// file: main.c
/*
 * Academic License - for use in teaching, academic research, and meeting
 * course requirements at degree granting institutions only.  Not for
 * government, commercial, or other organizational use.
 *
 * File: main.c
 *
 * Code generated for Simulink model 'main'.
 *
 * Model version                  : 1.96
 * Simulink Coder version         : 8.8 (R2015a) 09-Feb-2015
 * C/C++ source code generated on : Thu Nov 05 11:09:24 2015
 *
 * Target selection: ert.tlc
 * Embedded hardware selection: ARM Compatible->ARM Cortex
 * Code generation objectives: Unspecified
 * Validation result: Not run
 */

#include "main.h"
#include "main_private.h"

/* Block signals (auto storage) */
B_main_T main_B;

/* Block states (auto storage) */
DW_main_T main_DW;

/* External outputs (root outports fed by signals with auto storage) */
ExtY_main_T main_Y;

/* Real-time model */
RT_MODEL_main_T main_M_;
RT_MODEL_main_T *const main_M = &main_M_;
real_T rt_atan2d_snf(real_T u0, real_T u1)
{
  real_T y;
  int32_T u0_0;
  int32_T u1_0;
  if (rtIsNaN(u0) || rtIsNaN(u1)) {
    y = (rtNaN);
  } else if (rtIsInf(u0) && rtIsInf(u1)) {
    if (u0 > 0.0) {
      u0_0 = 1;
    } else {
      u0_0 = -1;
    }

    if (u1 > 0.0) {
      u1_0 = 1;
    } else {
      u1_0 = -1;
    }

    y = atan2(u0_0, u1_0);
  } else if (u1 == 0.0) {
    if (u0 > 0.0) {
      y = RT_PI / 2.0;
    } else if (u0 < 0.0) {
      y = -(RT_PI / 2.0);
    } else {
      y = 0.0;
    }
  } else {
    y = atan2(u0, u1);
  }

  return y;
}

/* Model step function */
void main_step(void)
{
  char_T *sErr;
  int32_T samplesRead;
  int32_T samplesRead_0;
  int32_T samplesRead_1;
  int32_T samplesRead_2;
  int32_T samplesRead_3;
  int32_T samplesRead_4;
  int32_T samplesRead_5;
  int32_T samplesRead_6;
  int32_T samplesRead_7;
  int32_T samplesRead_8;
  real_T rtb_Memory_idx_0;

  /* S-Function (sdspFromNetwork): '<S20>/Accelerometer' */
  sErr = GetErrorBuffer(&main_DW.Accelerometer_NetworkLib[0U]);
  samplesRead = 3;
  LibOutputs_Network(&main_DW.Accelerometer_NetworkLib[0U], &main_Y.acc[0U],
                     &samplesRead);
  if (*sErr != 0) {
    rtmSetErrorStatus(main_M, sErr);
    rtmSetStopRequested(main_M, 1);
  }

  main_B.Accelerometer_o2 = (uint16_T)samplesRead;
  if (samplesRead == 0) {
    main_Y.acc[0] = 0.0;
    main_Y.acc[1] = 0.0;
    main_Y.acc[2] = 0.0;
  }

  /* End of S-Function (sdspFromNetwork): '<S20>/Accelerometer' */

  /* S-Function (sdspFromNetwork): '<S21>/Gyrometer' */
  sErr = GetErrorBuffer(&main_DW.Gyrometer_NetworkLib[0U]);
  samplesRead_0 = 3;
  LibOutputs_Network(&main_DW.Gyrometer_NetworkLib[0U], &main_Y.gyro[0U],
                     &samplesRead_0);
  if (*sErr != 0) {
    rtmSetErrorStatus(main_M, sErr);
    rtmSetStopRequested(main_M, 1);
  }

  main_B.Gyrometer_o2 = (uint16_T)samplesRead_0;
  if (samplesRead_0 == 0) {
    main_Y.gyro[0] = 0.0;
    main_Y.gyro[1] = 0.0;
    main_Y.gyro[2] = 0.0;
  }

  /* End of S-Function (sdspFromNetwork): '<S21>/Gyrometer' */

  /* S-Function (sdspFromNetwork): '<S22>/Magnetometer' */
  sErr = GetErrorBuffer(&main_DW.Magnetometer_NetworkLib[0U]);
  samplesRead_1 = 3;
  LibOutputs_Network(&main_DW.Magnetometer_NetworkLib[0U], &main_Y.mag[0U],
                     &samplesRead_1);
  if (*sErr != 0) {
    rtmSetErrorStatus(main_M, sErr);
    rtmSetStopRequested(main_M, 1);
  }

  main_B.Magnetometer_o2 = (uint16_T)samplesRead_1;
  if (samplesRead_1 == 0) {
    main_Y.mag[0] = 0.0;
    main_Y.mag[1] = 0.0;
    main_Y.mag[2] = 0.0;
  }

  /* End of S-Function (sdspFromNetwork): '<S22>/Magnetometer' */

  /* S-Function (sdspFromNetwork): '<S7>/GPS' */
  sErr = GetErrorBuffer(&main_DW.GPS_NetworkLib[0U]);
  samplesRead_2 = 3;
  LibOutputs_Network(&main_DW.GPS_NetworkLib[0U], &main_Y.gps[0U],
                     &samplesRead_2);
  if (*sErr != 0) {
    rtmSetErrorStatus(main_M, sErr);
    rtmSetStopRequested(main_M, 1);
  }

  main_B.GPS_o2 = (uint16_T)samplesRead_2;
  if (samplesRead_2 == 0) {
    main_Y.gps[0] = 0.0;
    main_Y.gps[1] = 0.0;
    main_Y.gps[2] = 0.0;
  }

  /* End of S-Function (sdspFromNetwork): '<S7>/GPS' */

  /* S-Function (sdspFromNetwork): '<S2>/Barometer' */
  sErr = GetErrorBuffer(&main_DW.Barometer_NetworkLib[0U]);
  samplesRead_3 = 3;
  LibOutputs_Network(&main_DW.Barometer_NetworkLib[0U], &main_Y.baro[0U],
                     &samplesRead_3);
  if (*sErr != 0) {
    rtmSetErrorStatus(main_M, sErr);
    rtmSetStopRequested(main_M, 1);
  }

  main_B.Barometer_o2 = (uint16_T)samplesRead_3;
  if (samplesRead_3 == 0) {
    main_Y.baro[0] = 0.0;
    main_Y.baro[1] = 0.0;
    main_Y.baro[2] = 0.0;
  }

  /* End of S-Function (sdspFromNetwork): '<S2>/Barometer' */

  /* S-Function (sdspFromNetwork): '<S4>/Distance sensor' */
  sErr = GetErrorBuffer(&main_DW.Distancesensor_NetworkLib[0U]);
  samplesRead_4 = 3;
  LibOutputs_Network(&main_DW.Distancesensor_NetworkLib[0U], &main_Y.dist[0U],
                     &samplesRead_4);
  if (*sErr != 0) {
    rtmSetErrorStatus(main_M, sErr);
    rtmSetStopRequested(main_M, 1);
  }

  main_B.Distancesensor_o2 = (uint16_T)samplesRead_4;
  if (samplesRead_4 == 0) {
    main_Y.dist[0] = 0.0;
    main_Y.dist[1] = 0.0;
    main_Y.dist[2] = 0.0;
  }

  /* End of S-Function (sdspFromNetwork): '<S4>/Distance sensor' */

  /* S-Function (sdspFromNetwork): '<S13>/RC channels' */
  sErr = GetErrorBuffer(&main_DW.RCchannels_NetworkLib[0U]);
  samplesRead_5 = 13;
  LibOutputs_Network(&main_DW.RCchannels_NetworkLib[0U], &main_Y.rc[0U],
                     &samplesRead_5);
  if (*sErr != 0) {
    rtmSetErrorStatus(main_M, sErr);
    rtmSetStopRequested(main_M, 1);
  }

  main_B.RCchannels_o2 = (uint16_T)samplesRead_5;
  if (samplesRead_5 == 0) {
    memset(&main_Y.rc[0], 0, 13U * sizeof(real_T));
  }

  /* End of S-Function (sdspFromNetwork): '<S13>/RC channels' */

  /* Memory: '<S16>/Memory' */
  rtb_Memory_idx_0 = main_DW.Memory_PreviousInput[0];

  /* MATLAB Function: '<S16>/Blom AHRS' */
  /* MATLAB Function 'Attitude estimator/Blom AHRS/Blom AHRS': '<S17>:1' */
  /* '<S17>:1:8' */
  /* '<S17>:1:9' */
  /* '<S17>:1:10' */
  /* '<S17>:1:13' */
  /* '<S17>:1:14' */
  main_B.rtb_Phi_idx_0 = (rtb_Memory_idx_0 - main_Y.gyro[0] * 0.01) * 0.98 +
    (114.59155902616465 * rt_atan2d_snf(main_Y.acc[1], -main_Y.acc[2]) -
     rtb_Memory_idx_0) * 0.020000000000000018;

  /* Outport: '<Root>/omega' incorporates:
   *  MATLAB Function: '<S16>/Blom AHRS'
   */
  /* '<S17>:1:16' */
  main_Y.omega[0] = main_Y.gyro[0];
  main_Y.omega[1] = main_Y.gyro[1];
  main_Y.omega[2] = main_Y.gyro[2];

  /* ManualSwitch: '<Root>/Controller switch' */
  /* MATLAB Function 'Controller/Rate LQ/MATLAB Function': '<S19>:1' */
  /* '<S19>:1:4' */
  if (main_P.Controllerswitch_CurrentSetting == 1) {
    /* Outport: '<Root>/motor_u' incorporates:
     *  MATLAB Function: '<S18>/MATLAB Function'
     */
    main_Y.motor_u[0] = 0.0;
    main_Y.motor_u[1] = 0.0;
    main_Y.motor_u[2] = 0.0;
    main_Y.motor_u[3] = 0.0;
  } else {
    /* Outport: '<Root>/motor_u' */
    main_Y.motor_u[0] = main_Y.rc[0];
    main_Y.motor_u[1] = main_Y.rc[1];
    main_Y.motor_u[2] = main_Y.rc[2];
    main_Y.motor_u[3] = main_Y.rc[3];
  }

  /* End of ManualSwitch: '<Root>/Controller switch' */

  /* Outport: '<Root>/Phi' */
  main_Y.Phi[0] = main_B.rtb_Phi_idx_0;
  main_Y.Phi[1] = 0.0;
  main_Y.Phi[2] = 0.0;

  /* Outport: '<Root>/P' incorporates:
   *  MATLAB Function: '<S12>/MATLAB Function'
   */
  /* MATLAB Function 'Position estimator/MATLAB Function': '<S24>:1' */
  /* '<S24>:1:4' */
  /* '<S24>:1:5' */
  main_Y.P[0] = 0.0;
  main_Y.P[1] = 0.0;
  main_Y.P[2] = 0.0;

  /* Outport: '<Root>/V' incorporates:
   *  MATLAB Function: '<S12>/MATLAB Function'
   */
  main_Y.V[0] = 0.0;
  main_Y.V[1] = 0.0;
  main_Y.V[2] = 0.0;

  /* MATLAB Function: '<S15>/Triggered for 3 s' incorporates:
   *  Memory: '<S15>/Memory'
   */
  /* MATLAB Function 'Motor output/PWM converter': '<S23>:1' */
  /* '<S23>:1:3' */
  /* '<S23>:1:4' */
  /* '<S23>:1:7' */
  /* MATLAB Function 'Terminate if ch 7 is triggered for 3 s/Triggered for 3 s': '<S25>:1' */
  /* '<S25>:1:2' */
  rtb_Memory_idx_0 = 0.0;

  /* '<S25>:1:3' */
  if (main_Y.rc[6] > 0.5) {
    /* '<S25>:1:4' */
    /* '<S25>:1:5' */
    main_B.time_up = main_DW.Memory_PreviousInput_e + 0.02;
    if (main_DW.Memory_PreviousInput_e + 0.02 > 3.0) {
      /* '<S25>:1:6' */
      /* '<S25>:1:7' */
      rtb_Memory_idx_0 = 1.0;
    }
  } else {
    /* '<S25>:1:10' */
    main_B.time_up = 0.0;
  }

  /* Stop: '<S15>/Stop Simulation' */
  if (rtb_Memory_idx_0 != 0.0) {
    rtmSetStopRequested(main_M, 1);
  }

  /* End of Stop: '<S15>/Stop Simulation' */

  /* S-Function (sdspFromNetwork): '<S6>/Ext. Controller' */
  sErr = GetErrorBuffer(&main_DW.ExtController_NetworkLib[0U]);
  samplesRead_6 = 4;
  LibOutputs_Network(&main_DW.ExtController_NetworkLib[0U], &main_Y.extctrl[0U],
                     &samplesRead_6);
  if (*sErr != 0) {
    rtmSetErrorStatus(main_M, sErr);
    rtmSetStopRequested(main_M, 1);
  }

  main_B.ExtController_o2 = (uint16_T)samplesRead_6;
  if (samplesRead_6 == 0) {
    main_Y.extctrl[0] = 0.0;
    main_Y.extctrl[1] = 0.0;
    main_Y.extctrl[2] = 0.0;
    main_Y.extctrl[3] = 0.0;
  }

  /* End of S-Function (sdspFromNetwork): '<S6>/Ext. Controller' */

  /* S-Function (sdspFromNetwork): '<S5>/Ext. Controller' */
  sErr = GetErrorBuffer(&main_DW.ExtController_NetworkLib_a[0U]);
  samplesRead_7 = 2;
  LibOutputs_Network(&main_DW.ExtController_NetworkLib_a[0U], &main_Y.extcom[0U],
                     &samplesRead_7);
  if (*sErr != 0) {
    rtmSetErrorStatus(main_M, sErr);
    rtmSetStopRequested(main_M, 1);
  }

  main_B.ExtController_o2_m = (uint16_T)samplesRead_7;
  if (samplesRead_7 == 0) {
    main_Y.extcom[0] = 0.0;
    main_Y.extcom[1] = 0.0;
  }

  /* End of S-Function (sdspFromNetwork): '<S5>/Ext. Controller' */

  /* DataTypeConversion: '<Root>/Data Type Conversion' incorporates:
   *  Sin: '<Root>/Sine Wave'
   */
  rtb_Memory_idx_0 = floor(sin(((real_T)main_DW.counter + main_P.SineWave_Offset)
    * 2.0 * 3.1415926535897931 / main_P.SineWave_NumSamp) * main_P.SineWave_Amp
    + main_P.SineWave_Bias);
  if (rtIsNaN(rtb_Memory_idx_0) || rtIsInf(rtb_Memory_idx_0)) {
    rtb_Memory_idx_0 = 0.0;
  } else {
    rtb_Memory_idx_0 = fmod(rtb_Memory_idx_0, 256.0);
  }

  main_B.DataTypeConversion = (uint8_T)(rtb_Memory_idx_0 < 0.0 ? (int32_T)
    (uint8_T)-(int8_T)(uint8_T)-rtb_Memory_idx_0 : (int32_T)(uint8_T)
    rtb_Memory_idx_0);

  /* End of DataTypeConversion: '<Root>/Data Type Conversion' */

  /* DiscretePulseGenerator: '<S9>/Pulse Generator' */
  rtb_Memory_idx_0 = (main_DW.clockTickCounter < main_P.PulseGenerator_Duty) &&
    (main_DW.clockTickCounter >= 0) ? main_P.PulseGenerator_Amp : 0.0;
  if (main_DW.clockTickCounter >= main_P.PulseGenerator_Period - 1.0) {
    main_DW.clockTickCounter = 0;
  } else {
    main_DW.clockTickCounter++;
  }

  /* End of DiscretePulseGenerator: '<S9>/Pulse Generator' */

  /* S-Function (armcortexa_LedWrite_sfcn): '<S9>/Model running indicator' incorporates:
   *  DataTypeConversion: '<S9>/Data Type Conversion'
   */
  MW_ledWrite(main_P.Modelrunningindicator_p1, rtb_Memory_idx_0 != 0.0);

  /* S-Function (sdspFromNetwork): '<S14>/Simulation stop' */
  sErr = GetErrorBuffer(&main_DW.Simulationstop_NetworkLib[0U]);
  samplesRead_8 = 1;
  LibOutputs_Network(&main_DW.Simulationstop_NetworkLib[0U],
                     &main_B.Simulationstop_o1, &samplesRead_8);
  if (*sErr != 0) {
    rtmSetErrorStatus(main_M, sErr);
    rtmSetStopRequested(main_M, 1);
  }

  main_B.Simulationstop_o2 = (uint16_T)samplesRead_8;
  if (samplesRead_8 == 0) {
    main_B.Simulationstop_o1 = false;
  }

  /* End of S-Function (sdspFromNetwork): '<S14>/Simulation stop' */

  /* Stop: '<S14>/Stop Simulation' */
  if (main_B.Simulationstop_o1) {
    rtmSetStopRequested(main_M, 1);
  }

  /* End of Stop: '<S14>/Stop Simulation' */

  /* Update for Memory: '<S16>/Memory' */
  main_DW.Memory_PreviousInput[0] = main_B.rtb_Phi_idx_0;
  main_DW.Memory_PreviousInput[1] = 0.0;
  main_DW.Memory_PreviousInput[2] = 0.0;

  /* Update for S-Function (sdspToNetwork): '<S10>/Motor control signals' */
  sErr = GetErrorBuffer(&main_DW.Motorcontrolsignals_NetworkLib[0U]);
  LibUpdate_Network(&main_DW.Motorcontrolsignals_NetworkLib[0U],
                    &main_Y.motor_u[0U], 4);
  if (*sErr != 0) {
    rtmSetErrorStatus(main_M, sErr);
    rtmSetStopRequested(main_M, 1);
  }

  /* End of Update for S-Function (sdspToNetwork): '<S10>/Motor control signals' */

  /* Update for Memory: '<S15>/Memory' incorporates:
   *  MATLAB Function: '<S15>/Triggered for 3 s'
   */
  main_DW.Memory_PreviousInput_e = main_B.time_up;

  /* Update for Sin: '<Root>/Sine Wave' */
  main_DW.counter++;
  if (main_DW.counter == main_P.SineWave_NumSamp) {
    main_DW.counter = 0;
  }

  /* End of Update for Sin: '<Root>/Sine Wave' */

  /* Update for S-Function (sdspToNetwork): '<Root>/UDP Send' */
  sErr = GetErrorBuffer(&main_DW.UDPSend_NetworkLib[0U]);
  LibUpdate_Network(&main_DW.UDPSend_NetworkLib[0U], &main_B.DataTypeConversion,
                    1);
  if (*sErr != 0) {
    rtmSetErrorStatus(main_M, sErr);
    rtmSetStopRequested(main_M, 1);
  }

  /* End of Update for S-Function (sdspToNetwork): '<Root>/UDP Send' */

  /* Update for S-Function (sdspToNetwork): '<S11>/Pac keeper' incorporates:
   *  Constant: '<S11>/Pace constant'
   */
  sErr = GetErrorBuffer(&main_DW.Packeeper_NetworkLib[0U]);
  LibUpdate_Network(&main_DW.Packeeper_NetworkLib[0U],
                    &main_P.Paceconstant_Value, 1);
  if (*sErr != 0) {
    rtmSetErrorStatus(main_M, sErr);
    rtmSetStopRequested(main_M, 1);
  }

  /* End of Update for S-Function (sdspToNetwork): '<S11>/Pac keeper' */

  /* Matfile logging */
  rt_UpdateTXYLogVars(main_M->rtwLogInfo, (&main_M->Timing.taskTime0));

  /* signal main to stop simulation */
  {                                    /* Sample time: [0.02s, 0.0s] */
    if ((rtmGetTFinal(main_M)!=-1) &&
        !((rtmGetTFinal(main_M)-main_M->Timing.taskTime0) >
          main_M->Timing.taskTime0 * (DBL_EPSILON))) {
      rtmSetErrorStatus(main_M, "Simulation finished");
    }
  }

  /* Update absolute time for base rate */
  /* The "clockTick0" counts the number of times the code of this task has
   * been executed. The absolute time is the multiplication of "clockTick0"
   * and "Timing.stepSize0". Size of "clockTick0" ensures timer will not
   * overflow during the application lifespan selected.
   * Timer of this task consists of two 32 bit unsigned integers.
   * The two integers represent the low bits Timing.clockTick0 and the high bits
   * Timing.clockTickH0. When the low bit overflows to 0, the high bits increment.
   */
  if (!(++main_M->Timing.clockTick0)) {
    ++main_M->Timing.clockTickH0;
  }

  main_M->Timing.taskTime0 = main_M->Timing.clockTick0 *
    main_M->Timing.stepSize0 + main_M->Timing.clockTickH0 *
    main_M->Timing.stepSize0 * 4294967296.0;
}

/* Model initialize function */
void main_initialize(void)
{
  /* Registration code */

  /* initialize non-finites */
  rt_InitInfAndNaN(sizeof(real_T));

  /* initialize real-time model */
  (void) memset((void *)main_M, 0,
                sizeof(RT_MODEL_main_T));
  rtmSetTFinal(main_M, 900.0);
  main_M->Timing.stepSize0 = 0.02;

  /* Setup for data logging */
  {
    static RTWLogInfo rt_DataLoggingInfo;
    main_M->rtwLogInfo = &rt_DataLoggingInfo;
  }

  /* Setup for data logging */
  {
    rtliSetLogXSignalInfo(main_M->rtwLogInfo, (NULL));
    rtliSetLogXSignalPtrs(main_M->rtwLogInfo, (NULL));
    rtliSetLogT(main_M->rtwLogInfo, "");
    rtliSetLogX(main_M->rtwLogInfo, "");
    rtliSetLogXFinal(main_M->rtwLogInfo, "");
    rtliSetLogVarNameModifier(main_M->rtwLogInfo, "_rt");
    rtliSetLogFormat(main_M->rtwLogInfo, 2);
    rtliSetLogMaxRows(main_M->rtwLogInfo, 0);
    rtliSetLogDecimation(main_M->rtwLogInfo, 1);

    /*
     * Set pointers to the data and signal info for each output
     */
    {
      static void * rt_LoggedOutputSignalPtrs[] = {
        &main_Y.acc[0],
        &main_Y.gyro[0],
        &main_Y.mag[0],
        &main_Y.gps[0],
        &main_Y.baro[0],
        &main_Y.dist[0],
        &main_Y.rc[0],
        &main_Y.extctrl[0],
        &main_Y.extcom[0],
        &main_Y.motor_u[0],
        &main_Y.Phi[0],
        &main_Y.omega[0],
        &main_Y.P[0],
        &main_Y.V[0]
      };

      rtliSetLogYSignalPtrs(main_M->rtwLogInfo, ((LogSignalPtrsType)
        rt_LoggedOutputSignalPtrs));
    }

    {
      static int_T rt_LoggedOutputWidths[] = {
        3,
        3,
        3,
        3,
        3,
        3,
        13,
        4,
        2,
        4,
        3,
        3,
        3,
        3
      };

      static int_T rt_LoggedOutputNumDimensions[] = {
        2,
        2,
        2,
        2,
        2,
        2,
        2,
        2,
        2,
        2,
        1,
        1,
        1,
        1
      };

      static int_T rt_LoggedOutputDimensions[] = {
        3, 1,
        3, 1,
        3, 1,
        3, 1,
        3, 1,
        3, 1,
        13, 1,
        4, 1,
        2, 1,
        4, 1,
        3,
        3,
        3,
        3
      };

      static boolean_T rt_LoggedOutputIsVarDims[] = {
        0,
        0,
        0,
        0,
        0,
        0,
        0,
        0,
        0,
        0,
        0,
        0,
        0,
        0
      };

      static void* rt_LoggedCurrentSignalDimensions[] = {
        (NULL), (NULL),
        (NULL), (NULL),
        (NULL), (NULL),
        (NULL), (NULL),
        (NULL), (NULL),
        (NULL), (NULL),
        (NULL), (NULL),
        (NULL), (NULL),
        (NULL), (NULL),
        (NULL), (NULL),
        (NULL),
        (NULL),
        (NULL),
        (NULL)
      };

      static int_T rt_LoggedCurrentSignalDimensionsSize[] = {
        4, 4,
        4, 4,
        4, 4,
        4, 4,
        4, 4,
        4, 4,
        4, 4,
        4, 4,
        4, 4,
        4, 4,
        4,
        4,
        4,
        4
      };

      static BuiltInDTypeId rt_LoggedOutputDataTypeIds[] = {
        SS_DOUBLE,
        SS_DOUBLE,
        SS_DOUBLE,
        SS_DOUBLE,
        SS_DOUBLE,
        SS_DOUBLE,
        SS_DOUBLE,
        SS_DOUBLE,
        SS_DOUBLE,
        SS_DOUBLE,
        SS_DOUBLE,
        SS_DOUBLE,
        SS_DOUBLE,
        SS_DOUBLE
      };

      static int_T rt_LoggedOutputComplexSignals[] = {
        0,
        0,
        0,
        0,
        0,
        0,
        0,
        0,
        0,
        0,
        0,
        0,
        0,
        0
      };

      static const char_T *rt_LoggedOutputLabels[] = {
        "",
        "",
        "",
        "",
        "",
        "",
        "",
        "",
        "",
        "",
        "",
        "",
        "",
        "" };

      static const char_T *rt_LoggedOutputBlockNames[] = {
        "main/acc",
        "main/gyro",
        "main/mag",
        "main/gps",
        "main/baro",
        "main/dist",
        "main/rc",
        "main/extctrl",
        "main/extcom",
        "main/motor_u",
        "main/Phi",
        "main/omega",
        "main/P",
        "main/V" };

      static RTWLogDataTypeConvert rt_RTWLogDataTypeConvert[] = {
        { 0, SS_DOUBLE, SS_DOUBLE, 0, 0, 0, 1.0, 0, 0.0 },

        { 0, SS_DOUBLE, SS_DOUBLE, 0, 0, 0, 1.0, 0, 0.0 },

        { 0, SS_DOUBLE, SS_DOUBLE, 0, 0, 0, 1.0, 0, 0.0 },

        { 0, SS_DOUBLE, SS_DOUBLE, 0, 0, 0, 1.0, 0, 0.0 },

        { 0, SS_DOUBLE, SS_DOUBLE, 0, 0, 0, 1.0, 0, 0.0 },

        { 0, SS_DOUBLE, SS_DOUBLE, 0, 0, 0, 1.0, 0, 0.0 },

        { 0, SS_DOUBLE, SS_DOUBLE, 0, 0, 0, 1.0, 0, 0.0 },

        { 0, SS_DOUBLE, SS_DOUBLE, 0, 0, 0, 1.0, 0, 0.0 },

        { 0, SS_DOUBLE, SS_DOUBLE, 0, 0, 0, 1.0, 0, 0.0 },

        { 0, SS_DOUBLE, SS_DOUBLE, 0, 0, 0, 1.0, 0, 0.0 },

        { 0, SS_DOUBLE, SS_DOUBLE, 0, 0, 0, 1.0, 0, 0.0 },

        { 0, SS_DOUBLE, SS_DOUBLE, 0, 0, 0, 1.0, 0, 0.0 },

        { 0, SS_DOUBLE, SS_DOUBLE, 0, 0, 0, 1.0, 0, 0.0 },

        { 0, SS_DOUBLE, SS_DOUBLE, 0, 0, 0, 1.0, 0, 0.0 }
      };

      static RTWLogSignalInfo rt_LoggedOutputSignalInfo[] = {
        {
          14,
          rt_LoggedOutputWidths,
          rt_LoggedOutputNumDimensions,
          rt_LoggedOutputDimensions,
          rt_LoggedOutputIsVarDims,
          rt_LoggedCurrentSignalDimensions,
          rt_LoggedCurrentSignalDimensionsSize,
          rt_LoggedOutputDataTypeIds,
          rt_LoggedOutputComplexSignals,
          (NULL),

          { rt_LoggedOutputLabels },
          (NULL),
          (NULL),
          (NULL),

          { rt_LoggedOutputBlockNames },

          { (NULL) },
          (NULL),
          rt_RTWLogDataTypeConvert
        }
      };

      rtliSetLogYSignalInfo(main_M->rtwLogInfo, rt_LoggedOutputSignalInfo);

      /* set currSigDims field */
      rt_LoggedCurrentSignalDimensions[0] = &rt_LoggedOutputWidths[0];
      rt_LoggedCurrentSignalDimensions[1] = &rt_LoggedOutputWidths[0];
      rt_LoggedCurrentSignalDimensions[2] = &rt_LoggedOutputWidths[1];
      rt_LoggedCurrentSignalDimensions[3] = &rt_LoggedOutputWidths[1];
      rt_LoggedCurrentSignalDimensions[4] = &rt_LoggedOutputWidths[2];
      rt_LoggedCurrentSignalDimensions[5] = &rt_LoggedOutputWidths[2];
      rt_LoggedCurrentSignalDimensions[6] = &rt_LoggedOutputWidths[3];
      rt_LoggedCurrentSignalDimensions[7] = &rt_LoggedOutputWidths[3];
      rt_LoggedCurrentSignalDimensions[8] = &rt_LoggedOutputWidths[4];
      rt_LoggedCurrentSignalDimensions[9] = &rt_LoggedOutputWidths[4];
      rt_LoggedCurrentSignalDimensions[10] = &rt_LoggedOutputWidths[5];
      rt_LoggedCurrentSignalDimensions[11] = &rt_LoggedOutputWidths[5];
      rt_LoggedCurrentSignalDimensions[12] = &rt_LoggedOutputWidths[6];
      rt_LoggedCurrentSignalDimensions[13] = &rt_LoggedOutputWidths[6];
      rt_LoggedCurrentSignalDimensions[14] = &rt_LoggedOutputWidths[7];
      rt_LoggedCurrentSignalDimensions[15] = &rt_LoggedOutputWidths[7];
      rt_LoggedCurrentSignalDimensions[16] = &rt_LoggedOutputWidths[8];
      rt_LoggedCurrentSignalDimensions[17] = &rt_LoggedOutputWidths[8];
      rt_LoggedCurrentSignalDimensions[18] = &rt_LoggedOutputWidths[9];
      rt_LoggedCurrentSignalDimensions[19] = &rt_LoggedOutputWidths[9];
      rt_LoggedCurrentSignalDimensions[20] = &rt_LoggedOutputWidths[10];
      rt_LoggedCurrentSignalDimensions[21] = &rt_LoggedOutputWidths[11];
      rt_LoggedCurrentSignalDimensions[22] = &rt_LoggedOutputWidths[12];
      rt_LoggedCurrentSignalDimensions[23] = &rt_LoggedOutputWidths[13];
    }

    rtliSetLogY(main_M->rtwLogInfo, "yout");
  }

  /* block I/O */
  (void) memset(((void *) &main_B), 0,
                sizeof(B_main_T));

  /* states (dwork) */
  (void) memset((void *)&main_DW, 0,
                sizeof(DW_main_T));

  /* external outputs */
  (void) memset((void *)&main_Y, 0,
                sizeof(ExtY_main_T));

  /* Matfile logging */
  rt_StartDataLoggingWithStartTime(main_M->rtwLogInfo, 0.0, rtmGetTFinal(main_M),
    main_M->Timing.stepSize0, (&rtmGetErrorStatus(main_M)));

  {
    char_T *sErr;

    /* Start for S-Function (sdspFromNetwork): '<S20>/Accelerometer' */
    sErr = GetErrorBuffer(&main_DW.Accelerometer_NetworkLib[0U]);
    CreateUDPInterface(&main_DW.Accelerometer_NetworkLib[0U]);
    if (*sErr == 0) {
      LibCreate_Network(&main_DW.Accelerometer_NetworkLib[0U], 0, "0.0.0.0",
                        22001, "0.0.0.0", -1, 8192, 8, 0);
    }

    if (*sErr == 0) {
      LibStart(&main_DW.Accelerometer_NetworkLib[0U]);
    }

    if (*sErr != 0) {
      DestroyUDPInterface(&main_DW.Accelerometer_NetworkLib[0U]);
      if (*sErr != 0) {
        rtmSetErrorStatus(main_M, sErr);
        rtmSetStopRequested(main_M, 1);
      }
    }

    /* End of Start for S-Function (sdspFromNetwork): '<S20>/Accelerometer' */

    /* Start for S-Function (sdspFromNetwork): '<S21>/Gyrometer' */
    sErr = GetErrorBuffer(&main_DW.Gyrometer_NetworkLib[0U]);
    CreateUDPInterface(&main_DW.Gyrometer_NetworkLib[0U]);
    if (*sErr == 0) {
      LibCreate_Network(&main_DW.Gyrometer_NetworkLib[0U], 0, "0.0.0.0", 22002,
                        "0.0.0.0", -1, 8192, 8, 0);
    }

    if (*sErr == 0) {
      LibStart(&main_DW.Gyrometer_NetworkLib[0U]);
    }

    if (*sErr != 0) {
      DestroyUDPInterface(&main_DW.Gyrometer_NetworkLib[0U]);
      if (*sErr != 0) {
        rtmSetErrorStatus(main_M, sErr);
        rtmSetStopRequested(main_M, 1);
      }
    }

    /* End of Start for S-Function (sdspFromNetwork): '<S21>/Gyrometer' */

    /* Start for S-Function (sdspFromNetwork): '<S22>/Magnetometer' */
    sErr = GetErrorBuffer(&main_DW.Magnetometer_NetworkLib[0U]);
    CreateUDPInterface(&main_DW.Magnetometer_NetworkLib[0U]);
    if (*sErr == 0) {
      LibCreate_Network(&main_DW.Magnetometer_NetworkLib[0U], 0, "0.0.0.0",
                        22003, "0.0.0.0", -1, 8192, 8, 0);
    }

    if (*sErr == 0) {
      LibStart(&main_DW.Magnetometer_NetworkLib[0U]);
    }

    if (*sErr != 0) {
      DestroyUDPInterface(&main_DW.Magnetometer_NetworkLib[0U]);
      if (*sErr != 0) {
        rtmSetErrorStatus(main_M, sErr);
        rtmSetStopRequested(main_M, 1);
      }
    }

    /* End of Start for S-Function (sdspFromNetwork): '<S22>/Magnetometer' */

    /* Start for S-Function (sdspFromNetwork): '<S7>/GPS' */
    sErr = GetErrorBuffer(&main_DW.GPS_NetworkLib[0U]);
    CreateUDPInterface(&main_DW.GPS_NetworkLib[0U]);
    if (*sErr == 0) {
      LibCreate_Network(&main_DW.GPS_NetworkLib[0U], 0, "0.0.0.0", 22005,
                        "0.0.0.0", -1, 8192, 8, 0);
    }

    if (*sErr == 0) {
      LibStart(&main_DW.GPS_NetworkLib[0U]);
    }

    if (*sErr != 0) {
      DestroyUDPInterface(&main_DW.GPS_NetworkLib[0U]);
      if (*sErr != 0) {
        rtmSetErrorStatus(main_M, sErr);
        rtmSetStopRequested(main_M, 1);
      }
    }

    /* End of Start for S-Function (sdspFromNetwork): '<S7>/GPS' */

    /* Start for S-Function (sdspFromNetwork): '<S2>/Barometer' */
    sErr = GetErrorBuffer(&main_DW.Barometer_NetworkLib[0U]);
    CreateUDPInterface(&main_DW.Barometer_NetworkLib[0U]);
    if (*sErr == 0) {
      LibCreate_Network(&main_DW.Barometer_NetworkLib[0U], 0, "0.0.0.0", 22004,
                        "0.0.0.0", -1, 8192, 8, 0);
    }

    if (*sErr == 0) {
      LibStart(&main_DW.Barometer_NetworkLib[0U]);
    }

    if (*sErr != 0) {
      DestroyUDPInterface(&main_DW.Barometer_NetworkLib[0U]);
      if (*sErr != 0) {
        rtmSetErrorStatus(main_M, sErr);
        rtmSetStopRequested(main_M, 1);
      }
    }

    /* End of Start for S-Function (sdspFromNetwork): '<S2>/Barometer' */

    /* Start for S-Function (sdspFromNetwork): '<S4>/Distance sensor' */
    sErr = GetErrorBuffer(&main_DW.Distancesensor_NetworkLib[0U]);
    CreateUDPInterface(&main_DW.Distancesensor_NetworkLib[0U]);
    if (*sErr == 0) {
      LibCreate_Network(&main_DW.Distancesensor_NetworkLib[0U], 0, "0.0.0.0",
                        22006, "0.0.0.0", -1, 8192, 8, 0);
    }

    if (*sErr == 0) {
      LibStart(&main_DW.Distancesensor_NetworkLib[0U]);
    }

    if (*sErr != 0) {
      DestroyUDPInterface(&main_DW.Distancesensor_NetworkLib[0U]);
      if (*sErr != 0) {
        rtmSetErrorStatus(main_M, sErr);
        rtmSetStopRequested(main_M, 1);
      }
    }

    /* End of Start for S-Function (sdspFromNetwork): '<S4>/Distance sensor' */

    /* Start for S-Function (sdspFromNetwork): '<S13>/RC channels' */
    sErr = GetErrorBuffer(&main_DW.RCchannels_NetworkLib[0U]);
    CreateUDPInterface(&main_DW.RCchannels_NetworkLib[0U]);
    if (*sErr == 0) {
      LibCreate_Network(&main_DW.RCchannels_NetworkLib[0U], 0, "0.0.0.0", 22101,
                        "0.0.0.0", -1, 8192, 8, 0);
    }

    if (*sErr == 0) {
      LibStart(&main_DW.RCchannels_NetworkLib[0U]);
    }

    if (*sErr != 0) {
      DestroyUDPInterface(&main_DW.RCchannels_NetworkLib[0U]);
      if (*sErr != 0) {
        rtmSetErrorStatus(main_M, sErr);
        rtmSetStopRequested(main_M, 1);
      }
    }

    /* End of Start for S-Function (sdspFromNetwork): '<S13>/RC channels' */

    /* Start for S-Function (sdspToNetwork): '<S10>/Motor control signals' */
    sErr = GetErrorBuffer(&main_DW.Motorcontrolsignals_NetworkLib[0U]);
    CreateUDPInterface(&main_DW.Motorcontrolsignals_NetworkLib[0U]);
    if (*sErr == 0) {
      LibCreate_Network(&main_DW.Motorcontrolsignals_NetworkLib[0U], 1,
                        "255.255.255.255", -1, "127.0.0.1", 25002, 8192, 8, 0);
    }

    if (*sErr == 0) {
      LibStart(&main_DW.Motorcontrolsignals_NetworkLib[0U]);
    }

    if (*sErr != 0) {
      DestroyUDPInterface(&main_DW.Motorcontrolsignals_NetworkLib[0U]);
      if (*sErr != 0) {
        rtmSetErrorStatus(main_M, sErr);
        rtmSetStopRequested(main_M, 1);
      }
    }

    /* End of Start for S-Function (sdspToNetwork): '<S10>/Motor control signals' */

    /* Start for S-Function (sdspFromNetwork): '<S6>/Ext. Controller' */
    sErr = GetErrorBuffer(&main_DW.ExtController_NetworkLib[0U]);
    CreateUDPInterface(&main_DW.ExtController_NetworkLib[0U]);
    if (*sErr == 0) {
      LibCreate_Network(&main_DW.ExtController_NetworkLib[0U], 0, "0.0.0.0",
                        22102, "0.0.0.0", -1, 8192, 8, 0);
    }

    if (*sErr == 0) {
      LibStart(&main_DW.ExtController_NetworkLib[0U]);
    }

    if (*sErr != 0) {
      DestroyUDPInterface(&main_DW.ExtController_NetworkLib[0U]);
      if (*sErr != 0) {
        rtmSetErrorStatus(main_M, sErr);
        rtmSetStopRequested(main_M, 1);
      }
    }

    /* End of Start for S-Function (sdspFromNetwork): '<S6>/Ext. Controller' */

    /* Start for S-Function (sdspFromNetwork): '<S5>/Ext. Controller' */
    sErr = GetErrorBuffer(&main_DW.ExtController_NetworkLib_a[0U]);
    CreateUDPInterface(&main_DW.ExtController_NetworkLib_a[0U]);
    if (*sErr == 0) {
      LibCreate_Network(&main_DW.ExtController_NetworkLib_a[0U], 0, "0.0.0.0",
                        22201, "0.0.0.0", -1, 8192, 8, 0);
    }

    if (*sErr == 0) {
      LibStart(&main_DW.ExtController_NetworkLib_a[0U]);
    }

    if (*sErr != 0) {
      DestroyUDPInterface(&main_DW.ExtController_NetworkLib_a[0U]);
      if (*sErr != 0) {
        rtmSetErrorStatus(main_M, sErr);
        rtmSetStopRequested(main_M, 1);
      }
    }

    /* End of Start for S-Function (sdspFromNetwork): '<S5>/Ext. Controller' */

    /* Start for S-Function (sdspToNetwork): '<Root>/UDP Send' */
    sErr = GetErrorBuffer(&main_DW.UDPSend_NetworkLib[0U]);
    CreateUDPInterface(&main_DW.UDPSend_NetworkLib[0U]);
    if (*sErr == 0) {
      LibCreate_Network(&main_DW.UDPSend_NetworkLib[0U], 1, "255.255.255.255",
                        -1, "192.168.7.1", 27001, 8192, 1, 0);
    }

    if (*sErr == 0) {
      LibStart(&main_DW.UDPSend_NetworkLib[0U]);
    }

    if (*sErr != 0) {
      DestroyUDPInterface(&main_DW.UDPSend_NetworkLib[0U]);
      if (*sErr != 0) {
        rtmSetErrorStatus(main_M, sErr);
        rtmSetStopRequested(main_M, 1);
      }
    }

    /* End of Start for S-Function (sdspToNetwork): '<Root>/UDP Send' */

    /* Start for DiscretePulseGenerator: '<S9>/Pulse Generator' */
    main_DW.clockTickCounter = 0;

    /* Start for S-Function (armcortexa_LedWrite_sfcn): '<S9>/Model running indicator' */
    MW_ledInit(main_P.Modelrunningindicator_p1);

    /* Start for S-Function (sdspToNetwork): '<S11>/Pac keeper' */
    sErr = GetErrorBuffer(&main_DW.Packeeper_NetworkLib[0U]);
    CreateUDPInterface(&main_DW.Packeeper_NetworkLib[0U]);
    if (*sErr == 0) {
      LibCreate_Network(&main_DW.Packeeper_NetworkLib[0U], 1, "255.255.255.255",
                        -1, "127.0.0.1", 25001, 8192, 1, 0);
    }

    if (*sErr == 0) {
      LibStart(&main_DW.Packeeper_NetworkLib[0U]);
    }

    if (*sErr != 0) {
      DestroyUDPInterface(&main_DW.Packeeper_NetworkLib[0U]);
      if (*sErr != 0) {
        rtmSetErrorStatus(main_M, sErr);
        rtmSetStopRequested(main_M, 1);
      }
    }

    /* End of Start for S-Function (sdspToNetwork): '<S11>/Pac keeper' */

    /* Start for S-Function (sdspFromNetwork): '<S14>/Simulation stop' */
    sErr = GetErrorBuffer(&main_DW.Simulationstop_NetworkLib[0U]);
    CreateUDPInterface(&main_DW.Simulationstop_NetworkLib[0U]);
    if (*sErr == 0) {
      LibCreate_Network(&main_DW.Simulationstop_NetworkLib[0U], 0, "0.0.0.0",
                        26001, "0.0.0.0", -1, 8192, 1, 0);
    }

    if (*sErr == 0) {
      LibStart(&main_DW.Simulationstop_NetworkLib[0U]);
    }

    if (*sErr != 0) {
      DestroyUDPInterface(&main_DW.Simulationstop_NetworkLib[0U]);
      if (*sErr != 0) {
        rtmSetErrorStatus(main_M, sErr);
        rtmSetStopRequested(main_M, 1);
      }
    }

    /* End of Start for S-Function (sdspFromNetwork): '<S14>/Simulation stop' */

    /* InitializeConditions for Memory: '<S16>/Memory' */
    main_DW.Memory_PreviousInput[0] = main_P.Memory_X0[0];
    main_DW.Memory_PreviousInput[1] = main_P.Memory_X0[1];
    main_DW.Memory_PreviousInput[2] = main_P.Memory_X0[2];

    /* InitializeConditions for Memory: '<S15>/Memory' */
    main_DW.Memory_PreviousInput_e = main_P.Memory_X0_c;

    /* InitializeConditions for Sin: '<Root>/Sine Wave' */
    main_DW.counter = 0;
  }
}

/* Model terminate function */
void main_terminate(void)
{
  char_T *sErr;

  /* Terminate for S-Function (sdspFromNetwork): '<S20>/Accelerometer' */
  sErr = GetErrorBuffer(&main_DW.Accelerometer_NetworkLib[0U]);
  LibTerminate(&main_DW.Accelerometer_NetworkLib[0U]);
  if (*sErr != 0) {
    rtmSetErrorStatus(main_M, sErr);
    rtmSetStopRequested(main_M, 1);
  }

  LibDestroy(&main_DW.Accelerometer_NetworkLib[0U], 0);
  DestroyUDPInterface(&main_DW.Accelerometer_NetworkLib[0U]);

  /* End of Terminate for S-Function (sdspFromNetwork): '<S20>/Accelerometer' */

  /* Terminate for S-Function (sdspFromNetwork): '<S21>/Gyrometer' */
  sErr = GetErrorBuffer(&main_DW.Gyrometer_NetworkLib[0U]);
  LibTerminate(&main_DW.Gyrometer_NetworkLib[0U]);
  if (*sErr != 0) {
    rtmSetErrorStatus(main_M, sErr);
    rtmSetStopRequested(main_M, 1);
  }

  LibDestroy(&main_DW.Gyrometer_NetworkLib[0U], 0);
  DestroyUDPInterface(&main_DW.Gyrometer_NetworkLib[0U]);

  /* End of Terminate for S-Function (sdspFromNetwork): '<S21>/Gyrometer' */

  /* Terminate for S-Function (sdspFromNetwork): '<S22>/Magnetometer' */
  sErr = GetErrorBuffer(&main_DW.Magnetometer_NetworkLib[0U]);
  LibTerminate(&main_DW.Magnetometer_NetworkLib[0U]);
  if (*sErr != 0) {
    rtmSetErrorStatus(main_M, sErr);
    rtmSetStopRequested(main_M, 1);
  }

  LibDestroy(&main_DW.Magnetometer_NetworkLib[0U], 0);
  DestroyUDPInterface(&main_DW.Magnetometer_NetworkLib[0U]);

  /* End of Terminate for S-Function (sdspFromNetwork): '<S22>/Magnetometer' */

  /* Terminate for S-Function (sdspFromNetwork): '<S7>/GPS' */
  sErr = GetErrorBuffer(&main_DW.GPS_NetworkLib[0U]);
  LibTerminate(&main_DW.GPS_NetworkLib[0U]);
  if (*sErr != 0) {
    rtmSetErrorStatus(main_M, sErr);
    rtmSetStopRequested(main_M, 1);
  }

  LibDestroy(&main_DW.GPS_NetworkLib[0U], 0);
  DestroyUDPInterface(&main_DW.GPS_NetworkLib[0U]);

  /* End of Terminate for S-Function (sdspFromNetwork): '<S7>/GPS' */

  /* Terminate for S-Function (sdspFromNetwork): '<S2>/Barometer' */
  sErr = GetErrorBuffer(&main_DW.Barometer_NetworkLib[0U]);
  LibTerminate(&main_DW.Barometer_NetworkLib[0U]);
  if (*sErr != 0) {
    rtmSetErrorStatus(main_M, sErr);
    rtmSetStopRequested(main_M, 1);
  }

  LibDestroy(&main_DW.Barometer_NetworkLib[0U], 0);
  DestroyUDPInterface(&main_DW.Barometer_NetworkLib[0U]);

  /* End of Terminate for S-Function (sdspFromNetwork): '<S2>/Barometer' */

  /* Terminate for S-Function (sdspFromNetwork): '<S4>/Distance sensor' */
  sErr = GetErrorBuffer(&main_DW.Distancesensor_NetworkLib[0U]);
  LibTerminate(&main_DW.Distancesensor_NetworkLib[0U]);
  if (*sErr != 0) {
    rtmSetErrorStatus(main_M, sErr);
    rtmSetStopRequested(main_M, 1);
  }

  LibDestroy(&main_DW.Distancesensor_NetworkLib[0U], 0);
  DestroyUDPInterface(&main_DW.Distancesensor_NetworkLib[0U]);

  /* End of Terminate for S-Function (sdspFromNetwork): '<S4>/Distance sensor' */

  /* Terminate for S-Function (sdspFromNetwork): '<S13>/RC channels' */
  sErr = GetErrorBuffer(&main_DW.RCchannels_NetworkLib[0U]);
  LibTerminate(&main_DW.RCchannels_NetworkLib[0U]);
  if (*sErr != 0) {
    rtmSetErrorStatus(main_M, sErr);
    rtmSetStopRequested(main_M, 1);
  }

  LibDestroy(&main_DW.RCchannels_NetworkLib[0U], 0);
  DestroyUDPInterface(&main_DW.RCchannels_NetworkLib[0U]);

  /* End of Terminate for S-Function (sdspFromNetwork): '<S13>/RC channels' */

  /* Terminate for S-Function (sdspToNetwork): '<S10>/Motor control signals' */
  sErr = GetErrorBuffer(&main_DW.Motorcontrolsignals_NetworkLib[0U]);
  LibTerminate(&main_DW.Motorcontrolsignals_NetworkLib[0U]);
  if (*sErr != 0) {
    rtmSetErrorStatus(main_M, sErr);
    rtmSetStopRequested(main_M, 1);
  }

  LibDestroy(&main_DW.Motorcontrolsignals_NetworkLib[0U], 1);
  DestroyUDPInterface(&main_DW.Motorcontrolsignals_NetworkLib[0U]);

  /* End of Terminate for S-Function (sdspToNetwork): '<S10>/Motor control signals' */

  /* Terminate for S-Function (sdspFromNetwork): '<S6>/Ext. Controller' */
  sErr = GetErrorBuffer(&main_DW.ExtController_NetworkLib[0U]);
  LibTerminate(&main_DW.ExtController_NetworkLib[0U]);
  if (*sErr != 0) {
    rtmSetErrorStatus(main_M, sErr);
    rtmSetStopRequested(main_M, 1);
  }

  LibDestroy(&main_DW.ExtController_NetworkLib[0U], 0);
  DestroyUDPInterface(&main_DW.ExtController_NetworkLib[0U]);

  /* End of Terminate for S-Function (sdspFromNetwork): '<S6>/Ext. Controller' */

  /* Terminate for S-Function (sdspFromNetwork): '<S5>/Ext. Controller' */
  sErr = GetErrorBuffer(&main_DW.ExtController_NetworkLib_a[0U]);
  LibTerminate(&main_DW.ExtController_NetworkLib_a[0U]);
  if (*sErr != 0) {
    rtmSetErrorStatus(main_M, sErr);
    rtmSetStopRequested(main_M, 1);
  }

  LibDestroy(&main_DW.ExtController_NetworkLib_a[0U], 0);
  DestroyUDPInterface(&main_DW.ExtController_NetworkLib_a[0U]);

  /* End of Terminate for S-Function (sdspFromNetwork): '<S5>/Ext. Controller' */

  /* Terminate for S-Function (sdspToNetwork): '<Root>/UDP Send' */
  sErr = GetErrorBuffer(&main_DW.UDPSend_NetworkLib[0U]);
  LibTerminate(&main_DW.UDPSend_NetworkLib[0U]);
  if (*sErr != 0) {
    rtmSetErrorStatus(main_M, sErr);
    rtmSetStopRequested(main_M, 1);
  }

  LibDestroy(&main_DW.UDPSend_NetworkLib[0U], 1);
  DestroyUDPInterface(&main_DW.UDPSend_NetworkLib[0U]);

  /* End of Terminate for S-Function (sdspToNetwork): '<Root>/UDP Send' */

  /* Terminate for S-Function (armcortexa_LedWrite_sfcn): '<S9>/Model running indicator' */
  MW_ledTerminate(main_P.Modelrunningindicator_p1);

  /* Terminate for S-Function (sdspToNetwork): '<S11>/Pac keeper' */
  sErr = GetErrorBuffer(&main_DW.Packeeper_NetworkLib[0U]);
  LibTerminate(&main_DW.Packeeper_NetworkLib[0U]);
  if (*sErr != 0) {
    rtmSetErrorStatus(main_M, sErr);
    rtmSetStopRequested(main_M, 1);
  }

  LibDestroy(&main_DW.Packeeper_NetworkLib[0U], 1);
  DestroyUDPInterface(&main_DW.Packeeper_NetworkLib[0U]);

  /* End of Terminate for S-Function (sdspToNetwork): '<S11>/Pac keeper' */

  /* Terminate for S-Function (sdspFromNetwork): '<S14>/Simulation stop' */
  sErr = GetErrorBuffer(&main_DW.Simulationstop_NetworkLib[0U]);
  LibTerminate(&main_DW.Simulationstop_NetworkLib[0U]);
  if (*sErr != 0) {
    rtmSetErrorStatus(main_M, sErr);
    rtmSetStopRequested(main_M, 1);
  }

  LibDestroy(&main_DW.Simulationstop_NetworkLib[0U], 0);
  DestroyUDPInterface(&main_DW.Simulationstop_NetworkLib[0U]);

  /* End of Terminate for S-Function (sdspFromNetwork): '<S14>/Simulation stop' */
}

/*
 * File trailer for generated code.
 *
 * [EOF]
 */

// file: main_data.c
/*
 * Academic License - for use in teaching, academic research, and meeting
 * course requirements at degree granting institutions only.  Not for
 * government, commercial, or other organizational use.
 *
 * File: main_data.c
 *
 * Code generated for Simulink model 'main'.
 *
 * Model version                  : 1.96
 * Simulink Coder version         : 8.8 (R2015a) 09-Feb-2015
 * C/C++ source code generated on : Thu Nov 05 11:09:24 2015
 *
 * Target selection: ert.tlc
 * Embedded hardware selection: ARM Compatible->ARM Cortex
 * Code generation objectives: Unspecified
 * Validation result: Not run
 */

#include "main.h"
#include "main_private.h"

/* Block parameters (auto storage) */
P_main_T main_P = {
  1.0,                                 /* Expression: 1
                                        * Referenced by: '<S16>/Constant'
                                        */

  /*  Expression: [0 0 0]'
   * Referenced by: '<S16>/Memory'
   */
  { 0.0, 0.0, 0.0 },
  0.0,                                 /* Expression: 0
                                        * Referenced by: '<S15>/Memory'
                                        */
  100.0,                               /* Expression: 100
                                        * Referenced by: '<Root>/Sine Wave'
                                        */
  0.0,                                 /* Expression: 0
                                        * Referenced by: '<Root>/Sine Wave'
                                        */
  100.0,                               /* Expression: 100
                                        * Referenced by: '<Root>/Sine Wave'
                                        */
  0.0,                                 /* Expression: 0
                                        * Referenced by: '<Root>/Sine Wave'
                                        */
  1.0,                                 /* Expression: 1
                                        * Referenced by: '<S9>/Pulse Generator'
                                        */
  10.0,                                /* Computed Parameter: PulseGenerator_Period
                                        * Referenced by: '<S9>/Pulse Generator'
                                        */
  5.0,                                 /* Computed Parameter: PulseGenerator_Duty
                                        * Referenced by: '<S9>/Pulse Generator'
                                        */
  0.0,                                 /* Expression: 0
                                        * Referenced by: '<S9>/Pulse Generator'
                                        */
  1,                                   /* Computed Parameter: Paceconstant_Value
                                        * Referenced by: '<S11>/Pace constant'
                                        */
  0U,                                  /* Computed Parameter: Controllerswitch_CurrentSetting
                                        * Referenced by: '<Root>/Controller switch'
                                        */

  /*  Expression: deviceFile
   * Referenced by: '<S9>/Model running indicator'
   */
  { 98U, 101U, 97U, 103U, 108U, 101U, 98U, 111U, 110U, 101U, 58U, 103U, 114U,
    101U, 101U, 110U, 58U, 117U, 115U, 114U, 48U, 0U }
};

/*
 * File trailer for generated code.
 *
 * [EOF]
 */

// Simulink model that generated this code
simulink model "main"  (R2015a)
settings: Solver=ode3  StartTime=0.0  StopTime=time_end  FixedStep=time_step  RelTol=1e-3
values from neighbouring files (symbols this model uses):
  time_step = .02    (= 0.02)    [main.m]
libraries: dspnetwork x13, ec_arm_cortex_a_lib x1

== system main ==
  Attitude estimator : Subsystem  Variant=on  OverrideUsingVariant=Variant
  Barometer : Subsystem
  Controller : Subsystem  Variant=on  OverrideUsingVariant=Variant
  Controller switch : ManualSwitch  CurrentSetting=0
  Data Type Conversion : DataTypeConversion  OutDataTypeStr=uint8
  Distance sensor : Subsystem
  Ext. commands : Subsystem
  Ext. controller : Subsystem
  GPS : Subsystem
  IMU : Subsystem
  Model running indicator : Subsystem
  Motor output : Subsystem
  Pace keeper : Subsystem
  Position estimator : Subsystem
  RC channels : Subsystem
  Simulation stopper from UDP : Subsystem
  Sine Wave : Sin  SineType=Sample based  Amplitude=100  Samples=100  SampleTime=time_step  VectorParams1D=off
  Terminate if ch 7 is triggered for 3 s : Subsystem
  UDP Send : dspnetwork/UDP Send  remoteURL='192.168.7.1'  remotePort=27001  localURL='255.255.255.255'  localPortSource=Automatically determine  localPort=-1  sampletime=-1  blockPlatform=BeagleBone  separateLengthPort=0
  ch 1-4 : Selector  InputPortWidth=13  Indices=[1 2 3 4]
  acc : Outport
  gyro : Outport  Port=2
  mag : Outport  Port=3
  gps : Outport  Port=4
  baro : Outport  Port=5
  dist : Outport  Port=6
  rc : Outport  Port=7
  extctrl : Outport  Port=8
  extcom : Outport  Port=9
  motor_u : Outport  Port=10
  Phi : Outport  Port=11
  omega : Outport  Port=12
  P : Outport  Port=13
  V : Outport  Port=14
  wires:
  IMU/1(acc) -> acc/1, Attitude estimator/1(acc)
  IMU/2(gyro) -> gyro/1, Attitude estimator/2(gyro)
  IMU/3(mag) -> mag/1, Attitude estimator/3(mag)
  GPS/1(gps) -> gps/1, Position estimator/1(gps)
  Distance sensor/1(dist) -> Position estimator/3(dist), dist/1
  RC channels/1(rc) -> rc/1, Terminate if ch 7 is triggered for 3 s/1(channels), Controller/5(r), ch 1-4/1
  Ext. controller/1(extctrl) -> extctrl/1
  Ext. commands/1(extcom) -> extcom/1
  Position estimator/1(P) -> Controller/3(P), P/1
  Attitude estimator/1(Phi) -> Controller/1(Phi), Phi/1
  Attitude estimator/2(omega) -> omega/1, Controller/2(omega)
  Position estimator/2(V) -> V/1, Controller/4(V)
  Controller/1(motor_u) -> Controller switch/1
  Barometer/1(baro) -> baro/1, Position estimator/2(baro)
  Controller switch/1 -> motor_u/1, Motor output/1(motor_u)
  ch 1-4/1 -> Controller switch/2
  Sine Wave/1 -> Data Type Conversion/1
  Data Type Conversion/1 -> UDP Send/1

== system main/Attitude estimator ==
  note: 1) Add Subsystem or Model blocks as valid variant choices.
      | 2) You cannot connect blocks at this level. At simulation, connectivity is automatically
      | determined, based on the active variant and port name matching.
  acc : Inport
  gyro : Inport  Port=2
  mag : Inport  Port=3
  Blom AHRS : Subsystem  VariantControl=Variant
  Phi : Outport
  omega : Outport  Port=2

== system main/Barometer ==
  Barometer : dspnetwork/UDP Receive  localURL='0.0.0.0'  localPort=22004  remoteURL='0.0.0.0'  remotePort=-1  recvBufferSize=8192  dims=3  signalDatatype=double  isVarSize=off  showBlockingTime=on  blockingTime=0  sampletime=time_step  blockPlatform=BeagleBone
  Terminator : Terminator
  baro : Outport
  wires:
  Barometer/2 -> Terminator/1
  Barometer/1 -> baro/1

== system main/Controller ==
  note: 1) Add Subsystem or Model blocks as valid variant choices.
      | 2) You cannot connect blocks at this level. At simulation, connectivity is automatically
      | determined, based on the active variant and port name matching.
  Phi : Inport
  omega : Inport  Port=2
  P : Inport  Port=3
  V : Inport  Port=4
  r : Inport  Port=5
  Rate LQ : Subsystem  VariantControl=Variant
  motor_u : Outport

== system main/Distance sensor ==
  Distance sensor : dspnetwork/UDP Receive  localURL='0.0.0.0'  localPort=22006  remoteURL='0.0.0.0'  remotePort=-1  recvBufferSize=8192  dims=3  signalDatatype=double  isVarSize=off  showBlockingTime=on  blockingTime=0  sampletime=time_step  blockPlatform=BeagleBone
  Terminator : Terminator
  dist : Outport
  wires:
  Distance sensor/2 -> Terminator/1
  Distance sensor/1 -> dist/1

== system main/Ext. commands ==
  Ext. Controller : dspnetwork/UDP Receive  localURL='0.0.0.0'  localPort=22201  remoteURL='0.0.0.0'  remotePort=-1  recvBufferSize=8192  dims=2  signalDatatype=double  isVarSize=off  showBlockingTime=on  blockingTime=0  sampletime=time_step  blockPlatform=BeagleBone
  Terminator : Terminator
  extcom : Outport
  wires:
  Ext. Controller/2 -> Terminator/1
  Ext. Controller/1 -> extcom/1

== system main/Ext. controller ==
  Ext. Controller : dspnetwork/UDP Receive  localURL='0.0.0.0'  localPort=22102  remoteURL='0.0.0.0'  remotePort=-1  recvBufferSize=8192  dims=4  signalDatatype=double  isVarSize=off  showBlockingTime=on  blockingTime=0  sampletime=time_step  blockPlatform=BeagleBone
  Terminator : Terminator
  extctrl : Outport
  wires:
  Ext. Controller/2 -> Terminator/1
  Ext. Controller/1 -> extctrl/1

== system main/GPS ==
  GPS : dspnetwork/UDP Receive  localURL='0.0.0.0'  localPort=22005  remoteURL='0.0.0.0'  remotePort=-1  recvBufferSize=8192  dims=3  signalDatatype=double  isVarSize=off  showBlockingTime=on  blockingTime=0  sampletime=time_step  blockPlatform=BeagleBone
  Terminator : Terminator
  gps : Outport
  wires:
  GPS/2 -> Terminator/1
  GPS/1 -> gps/1

== system main/IMU ==
  Accelerometer : Subsystem
  Gyrometer : Subsystem
  Magnetometer : Subsystem
  acc : Outport
  gyro : Outport  Port=2
  mag : Outport  Port=3
  wires:
  Magnetometer/1(mag) -> mag/1
  Gyrometer/1(gyro) -> gyro/1
  Accelerometer/1(acc) -> acc/1

== system main/Model running indicator ==
  Data Type Conversion : DataTypeConversion  OutDataTypeStr=boolean
  Model running indicator : ec_arm_cortex_a_lib/LED  board=BeagleBone Black  led=USR0  blockPlatform=BeagleBone
  Pulse Generator : DiscretePulseGenerator  PulseType=Time based  Period=.2  PulseWidth=50
  wires:
  Data Type Conversion/1 -> Model running indicator/1
  Pulse Generator/1 -> Data Type Conversion/1

== system main/Motor output ==
  motor_u : Inport
  Data Type Conversion : DataTypeConversion  OutDataTypeStr=double  LockScale=on
  Motor control signals : dspnetwork/UDP Send  remoteURL='127.0.0.1'  remotePort=25002  localURL='255.255.255.255'  localPortSource=Automatically determine  localPort=-1  sampletime=-1  blockPlatform=BeagleBone  separateLengthPort=0
  PWM converter : MATLAB Function  TreatAsAtomicUnit=on
  Terminator : Terminator
  wires:
  motor_u/1 -> Data Type Conversion/1, PWM converter/1(motor_u)
  PWM converter/1(pwm_signals) -> Terminator/1
  Data Type Conversion/1 -> Motor control signals/1

== system main/Pace keeper ==
  Pac keeper : dspnetwork/UDP Send  remoteURL='127.0.0.1'  remotePort=25001  localURL='255.255.255.255'  localPortSource=Automatically determine  localPort=-1  sampletime=-1  blockPlatform=BeagleBone  separateLengthPort=0
  Pace constant : Constant  OutDataTypeStr=int8
  wires:
  Pace constant/1 -> Pac keeper/1

== system main/Position estimator ==
  gps : Inport
  baro : Inport  Port=2
  dist : Inport  Port=3
  MATLAB Function : MATLAB Function  TreatAsAtomicUnit=on
  P : Outport
  V : Outport  Port=2
  wires:
  baro/1 -> MATLAB Function/2(baro)
  dist/1 -> MATLAB Function/3(dist)
  gps/1 -> MATLAB Function/1(gps)
  MATLAB Function/1(P) -> P/1
  MATLAB Function/2(V) -> V/1

== system main/RC channels ==
  RC channels : dspnetwork/UDP Receive  localURL='0.0.0.0'  localPort=22101  remoteURL='0.0.0.0'  remotePort=-1  recvBufferSize=8192  dims=13  signalDatatype=double  isVarSize=off  showBlockingTime=on  blockingTime=0  sampletime=time_step  blockPlatform=BeagleBone
  Terminator : Terminator
  rc : Outport
  wires:
  RC channels/2 -> Terminator/1
  RC channels/1 -> rc/1

== system main/Simulation stopper from UDP ==
  Simulation stop : dspnetwork/UDP Receive  localURL='0.0.0.0'  localPort=26001  remoteURL='0.0.0.0'  remotePort=-1  recvBufferSize=8192  dims=1  signalDatatype=boolean  isVarSize=off  showBlockingTime=on  blockingTime=0  sampletime=0.02  blockPlatform=BeagleBone
  Stop Simulation : Stop
  Terminator2 : Terminator
  wires:
  Simulation stop/1 -> Stop Simulation/1
  Simulation stop/2 -> Terminator2/1

== system main/Terminate if ch 7 is triggered for 3 s ==
  channels : Inport
  Channel 7 : Selector  InputPortWidth=13  Indices=[7]
  Memory : Memory
  Stop Simulation : Stop
  Triggered for 3 s : MATLAB Function  TreatAsAtomicUnit=on
  wires:
  Triggered for 3 s/1(y) -> Stop Simulation/1
  Channel 7/1 -> Triggered for 3 s/1(ch7)
  Memory/1 -> Triggered for 3 s/2(time_up_last)
  Triggered for 3 s/2(time_up) -> Memory/1
  channels/1 -> Channel 7/1

== system main/Attitude estimator/Blom AHRS ==
  acc : Inport
  gyro : Inport  Port=2
  mag : Inport  Port=3
  Blom AHRS : MATLAB Function  TreatAsAtomicUnit=on
  Constant : Constant
  Memory : Memory  X0=[0 0 0]'
  Terminator : Terminator
  Phi : Outport
  omega : Outport  Port=2
  wires:
  gyro/1 -> Blom AHRS/2(gyro)
  acc/1 -> Blom AHRS/1(acc)
  Blom AHRS/1(Phi) -> Memory/1, Phi/1
  Blom AHRS/2(omega) -> omega/1
  Memory/1 -> Blom AHRS/4(Phi_last)
  mag/1 -> Terminator/1
  Constant/1 -> Blom AHRS/3(mag)

== system main/Controller/Rate LQ ==
  Phi : Inport
  omega : Inport  Port=2
  P : Inport  Port=3
  V : Inport  Port=4
  r : Inport  Port=5
  MATLAB Function : MATLAB Function  TreatAsAtomicUnit=on
  Terminator : Terminator
  Terminator1 : Terminator
  Terminator2 : Terminator
  motor_u : Outport
  wires:
  P/1 -> Terminator/1
  MATLAB Function/1(motor_u) -> motor_u/1
  r/1 -> MATLAB Function/2(r)
  omega/1 -> MATLAB Function/1(omega)
  V/1 -> Terminator2/1
  Phi/1 -> Terminator1/1

== system main/IMU/Accelerometer ==
  Accelerometer : dspnetwork/UDP Receive  localURL='0.0.0.0'  localPort=22001  remoteURL='0.0.0.0'  remotePort=-1  recvBufferSize=8192  dims=3  signalDatatype=double  isVarSize=off  showBlockingTime=on  blockingTime=0  sampletime=time_step  blockPlatform=BeagleBone
  Terminator : Terminator
  acc : Outport
  wires:
  Accelerometer/2 -> Terminator/1
  Accelerometer/1 -> acc/1

== system main/IMU/Gyrometer ==
  Gyrometer : dspnetwork/UDP Receive  localURL='0.0.0.0'  localPort=22002  remoteURL='0.0.0.0'  remotePort=-1  recvBufferSize=8192  dims=3  signalDatatype=double  isVarSize=off  showBlockingTime=on  blockingTime=0  sampletime=time_step  blockPlatform=BeagleBone
  Terminator : Terminator
  gyro : Outport
  wires:
  Gyrometer/2 -> Terminator/1
  Gyrometer/1 -> gyro/1

== system main/IMU/Magnetometer ==
  Magnetometer : dspnetwork/UDP Receive  localURL='0.0.0.0'  localPort=22003  remoteURL='0.0.0.0'  remotePort=-1  recvBufferSize=8192  dims=3  signalDatatype=double  isVarSize=off  showBlockingTime=on  blockingTime=0  sampletime=time_step  blockPlatform=BeagleBone
  Terminator : Terminator
  mag : Outport
  wires:
  Magnetometer/2 -> Terminator/1
  Magnetometer/1 -> mag/1

== matlab function main/Attitude estimator/Blom AHRS/Blom AHRS ==
function [Phi, omega] = fcn(acc, gyro, mag, Phi_last)
%#codegen

pg = .98;
pa = 1-pg;
dt = 0.01;

ay = acc(2);
az = acc(3);
gx = gyro(1);

Phi = [0 0 0]';
Phi(1) = pg*(Phi_last(1) - gx*dt) + pa*((360/pi)*atan2(ay,-az) - Phi_last(1));

omega = gyro;

== matlab function main/Position estimator/MATLAB Function ==
function [P, V] = fcn(gps, baro, dist)
%#codegen

P = [0 0 0]';
V = [0 0 0]';

== matlab function main/Controller/Rate LQ/MATLAB Function ==
function motor_u = fcn(omega, r)
%#codegen

motor_u = [0 0 0 0]';

== matlab function main/Motor output/PWM converter ==
function pwm_signals = fcn(motor_u)
%#codegen
pulse_min = 1100*1e-6;
pulse_max = 1930*1e-6;
pulse_f = 50;

pwm_signals = pulse_f * (pulse_min + motor_u .* (pulse_max - pulse_min));

== matlab function main/Terminate if ch 7 is triggered for 3 s/Triggered for 3 s ==
function [y, time_up] = fcn(ch7, time_up_last)
y = 0;
time_step = 0.02;
if ch7 > 0.5
    time_up = time_up_last + time_step;
    if time_up > 3
        y = 1;
    end
else
    time_up = 0;
end
